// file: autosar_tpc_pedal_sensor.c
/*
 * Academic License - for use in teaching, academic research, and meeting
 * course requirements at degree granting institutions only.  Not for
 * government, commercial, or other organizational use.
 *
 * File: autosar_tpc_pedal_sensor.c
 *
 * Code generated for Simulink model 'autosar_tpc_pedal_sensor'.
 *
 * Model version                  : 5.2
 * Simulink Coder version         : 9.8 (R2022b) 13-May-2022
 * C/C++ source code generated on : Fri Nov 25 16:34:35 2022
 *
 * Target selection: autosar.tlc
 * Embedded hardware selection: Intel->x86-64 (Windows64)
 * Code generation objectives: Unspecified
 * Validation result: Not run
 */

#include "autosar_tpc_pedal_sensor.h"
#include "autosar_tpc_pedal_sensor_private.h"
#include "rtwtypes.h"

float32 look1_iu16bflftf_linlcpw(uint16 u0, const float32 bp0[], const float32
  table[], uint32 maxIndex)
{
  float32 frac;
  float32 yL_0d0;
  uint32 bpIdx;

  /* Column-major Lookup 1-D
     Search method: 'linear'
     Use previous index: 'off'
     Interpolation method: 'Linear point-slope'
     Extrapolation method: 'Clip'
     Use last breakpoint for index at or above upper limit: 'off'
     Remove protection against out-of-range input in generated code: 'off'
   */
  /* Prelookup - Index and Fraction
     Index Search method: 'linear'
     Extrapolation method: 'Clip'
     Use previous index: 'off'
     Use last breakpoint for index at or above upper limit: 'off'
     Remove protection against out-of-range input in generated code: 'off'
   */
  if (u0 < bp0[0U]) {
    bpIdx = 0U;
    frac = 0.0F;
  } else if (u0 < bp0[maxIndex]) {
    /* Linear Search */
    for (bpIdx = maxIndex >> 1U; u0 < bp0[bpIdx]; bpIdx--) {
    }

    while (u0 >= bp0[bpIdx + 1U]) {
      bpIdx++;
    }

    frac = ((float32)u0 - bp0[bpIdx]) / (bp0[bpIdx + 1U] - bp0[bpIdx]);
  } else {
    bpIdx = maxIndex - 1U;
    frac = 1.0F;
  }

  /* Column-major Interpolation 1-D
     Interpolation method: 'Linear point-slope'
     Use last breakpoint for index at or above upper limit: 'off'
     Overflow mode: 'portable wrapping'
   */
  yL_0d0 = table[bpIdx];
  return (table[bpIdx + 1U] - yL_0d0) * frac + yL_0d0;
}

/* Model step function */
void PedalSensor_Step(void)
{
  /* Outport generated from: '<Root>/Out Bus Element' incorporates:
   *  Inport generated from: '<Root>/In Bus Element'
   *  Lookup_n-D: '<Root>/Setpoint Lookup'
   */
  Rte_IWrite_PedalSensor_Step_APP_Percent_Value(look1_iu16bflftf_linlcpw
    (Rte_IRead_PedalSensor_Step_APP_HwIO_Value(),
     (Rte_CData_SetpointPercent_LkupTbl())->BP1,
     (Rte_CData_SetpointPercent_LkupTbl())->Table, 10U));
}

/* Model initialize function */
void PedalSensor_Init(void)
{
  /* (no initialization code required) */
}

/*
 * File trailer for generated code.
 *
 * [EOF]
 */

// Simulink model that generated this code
simulink model "autosar_tpc_pedal_sensor"  (R2022a)
settings: Solver=FixedStepDiscrete  StartTime=0.0  StopTime=10.0  FixedStep=0.005  RelTol=1e-3
model workspace (MATLAB code in the model file):
  | SetpointPercent_LkupTbl = Simulink.LookupTable;
  | SetpointPercent_LkupTbl.Table.DataType = 'single';
  | SetpointPercent_LkupTbl.Table.FieldName = 'Table';
  | SetpointPercent_LkupTbl.Table.Value = ...
  |   [0 10 20 30 40 50 60 70 80 90 100];
  | SetpointPercent_LkupTbl.BreakpointsSpecification = 'Explicit values';
  | SetpointPercent_LkupTbl.SupportTunableSize = false;
  | SetpointPercent_LkupTbl.Breakpoints.DataType = 'single';
  | SetpointPercent_LkupTbl.Breakpoints.FieldName = 'BP1';
  | SetpointPercent_LkupTbl.Breakpoints.Value = ...
  |   single(linspace(170, 985, 11));
  | SetpointPercent_LkupTbl.Breakpoints.TunableSizeName = 'N1';
  | SetpointPercent_LkupTbl.StructTypeInfo.Name = 'MyStruct';
  | SetpointPercent_LkupTbl.StructTypeInfo.HeaderFileName = 'Rte_Type.h';
undefined symbols (not defined in the file or in its folder): TPSPercentBkpt, TPSPercentTbl

== system autosar_tpc_pedal_sensor ==
  note: Copyright 2019 The MathWorks, Inc.
  In Bus Element : Inport  PortName=APP_HwIO  Element=Value
  Setpoint Lookup : Lookup_n-D  NumberOfTableDimensions=1  DataSpecification=Lookup table object  LookupTableObject=SetpointPercent_LkupTbl  BreakpointsForDimension1=TPSPercentBkpt  BreakpointsForDimension1DataTypeStr=single  IndexSearchMethod=Linear search  Table=TPSPercentTbl  TableDataTypeStr=single  ExtrapMethod=Clip  InternalRulePriority=Speed  OutDataTypeStr=single  RndMeth=Simplest
  Out Bus Element : Outport  VectorParamsAs1DForOutWhenUnconnected=off  PortName=APP_Percent  Element=Value
  wires:
  In Bus Element/1 -> Setpoint Lookup/1
  Setpoint Lookup/1 -> Out Bus Element/1
